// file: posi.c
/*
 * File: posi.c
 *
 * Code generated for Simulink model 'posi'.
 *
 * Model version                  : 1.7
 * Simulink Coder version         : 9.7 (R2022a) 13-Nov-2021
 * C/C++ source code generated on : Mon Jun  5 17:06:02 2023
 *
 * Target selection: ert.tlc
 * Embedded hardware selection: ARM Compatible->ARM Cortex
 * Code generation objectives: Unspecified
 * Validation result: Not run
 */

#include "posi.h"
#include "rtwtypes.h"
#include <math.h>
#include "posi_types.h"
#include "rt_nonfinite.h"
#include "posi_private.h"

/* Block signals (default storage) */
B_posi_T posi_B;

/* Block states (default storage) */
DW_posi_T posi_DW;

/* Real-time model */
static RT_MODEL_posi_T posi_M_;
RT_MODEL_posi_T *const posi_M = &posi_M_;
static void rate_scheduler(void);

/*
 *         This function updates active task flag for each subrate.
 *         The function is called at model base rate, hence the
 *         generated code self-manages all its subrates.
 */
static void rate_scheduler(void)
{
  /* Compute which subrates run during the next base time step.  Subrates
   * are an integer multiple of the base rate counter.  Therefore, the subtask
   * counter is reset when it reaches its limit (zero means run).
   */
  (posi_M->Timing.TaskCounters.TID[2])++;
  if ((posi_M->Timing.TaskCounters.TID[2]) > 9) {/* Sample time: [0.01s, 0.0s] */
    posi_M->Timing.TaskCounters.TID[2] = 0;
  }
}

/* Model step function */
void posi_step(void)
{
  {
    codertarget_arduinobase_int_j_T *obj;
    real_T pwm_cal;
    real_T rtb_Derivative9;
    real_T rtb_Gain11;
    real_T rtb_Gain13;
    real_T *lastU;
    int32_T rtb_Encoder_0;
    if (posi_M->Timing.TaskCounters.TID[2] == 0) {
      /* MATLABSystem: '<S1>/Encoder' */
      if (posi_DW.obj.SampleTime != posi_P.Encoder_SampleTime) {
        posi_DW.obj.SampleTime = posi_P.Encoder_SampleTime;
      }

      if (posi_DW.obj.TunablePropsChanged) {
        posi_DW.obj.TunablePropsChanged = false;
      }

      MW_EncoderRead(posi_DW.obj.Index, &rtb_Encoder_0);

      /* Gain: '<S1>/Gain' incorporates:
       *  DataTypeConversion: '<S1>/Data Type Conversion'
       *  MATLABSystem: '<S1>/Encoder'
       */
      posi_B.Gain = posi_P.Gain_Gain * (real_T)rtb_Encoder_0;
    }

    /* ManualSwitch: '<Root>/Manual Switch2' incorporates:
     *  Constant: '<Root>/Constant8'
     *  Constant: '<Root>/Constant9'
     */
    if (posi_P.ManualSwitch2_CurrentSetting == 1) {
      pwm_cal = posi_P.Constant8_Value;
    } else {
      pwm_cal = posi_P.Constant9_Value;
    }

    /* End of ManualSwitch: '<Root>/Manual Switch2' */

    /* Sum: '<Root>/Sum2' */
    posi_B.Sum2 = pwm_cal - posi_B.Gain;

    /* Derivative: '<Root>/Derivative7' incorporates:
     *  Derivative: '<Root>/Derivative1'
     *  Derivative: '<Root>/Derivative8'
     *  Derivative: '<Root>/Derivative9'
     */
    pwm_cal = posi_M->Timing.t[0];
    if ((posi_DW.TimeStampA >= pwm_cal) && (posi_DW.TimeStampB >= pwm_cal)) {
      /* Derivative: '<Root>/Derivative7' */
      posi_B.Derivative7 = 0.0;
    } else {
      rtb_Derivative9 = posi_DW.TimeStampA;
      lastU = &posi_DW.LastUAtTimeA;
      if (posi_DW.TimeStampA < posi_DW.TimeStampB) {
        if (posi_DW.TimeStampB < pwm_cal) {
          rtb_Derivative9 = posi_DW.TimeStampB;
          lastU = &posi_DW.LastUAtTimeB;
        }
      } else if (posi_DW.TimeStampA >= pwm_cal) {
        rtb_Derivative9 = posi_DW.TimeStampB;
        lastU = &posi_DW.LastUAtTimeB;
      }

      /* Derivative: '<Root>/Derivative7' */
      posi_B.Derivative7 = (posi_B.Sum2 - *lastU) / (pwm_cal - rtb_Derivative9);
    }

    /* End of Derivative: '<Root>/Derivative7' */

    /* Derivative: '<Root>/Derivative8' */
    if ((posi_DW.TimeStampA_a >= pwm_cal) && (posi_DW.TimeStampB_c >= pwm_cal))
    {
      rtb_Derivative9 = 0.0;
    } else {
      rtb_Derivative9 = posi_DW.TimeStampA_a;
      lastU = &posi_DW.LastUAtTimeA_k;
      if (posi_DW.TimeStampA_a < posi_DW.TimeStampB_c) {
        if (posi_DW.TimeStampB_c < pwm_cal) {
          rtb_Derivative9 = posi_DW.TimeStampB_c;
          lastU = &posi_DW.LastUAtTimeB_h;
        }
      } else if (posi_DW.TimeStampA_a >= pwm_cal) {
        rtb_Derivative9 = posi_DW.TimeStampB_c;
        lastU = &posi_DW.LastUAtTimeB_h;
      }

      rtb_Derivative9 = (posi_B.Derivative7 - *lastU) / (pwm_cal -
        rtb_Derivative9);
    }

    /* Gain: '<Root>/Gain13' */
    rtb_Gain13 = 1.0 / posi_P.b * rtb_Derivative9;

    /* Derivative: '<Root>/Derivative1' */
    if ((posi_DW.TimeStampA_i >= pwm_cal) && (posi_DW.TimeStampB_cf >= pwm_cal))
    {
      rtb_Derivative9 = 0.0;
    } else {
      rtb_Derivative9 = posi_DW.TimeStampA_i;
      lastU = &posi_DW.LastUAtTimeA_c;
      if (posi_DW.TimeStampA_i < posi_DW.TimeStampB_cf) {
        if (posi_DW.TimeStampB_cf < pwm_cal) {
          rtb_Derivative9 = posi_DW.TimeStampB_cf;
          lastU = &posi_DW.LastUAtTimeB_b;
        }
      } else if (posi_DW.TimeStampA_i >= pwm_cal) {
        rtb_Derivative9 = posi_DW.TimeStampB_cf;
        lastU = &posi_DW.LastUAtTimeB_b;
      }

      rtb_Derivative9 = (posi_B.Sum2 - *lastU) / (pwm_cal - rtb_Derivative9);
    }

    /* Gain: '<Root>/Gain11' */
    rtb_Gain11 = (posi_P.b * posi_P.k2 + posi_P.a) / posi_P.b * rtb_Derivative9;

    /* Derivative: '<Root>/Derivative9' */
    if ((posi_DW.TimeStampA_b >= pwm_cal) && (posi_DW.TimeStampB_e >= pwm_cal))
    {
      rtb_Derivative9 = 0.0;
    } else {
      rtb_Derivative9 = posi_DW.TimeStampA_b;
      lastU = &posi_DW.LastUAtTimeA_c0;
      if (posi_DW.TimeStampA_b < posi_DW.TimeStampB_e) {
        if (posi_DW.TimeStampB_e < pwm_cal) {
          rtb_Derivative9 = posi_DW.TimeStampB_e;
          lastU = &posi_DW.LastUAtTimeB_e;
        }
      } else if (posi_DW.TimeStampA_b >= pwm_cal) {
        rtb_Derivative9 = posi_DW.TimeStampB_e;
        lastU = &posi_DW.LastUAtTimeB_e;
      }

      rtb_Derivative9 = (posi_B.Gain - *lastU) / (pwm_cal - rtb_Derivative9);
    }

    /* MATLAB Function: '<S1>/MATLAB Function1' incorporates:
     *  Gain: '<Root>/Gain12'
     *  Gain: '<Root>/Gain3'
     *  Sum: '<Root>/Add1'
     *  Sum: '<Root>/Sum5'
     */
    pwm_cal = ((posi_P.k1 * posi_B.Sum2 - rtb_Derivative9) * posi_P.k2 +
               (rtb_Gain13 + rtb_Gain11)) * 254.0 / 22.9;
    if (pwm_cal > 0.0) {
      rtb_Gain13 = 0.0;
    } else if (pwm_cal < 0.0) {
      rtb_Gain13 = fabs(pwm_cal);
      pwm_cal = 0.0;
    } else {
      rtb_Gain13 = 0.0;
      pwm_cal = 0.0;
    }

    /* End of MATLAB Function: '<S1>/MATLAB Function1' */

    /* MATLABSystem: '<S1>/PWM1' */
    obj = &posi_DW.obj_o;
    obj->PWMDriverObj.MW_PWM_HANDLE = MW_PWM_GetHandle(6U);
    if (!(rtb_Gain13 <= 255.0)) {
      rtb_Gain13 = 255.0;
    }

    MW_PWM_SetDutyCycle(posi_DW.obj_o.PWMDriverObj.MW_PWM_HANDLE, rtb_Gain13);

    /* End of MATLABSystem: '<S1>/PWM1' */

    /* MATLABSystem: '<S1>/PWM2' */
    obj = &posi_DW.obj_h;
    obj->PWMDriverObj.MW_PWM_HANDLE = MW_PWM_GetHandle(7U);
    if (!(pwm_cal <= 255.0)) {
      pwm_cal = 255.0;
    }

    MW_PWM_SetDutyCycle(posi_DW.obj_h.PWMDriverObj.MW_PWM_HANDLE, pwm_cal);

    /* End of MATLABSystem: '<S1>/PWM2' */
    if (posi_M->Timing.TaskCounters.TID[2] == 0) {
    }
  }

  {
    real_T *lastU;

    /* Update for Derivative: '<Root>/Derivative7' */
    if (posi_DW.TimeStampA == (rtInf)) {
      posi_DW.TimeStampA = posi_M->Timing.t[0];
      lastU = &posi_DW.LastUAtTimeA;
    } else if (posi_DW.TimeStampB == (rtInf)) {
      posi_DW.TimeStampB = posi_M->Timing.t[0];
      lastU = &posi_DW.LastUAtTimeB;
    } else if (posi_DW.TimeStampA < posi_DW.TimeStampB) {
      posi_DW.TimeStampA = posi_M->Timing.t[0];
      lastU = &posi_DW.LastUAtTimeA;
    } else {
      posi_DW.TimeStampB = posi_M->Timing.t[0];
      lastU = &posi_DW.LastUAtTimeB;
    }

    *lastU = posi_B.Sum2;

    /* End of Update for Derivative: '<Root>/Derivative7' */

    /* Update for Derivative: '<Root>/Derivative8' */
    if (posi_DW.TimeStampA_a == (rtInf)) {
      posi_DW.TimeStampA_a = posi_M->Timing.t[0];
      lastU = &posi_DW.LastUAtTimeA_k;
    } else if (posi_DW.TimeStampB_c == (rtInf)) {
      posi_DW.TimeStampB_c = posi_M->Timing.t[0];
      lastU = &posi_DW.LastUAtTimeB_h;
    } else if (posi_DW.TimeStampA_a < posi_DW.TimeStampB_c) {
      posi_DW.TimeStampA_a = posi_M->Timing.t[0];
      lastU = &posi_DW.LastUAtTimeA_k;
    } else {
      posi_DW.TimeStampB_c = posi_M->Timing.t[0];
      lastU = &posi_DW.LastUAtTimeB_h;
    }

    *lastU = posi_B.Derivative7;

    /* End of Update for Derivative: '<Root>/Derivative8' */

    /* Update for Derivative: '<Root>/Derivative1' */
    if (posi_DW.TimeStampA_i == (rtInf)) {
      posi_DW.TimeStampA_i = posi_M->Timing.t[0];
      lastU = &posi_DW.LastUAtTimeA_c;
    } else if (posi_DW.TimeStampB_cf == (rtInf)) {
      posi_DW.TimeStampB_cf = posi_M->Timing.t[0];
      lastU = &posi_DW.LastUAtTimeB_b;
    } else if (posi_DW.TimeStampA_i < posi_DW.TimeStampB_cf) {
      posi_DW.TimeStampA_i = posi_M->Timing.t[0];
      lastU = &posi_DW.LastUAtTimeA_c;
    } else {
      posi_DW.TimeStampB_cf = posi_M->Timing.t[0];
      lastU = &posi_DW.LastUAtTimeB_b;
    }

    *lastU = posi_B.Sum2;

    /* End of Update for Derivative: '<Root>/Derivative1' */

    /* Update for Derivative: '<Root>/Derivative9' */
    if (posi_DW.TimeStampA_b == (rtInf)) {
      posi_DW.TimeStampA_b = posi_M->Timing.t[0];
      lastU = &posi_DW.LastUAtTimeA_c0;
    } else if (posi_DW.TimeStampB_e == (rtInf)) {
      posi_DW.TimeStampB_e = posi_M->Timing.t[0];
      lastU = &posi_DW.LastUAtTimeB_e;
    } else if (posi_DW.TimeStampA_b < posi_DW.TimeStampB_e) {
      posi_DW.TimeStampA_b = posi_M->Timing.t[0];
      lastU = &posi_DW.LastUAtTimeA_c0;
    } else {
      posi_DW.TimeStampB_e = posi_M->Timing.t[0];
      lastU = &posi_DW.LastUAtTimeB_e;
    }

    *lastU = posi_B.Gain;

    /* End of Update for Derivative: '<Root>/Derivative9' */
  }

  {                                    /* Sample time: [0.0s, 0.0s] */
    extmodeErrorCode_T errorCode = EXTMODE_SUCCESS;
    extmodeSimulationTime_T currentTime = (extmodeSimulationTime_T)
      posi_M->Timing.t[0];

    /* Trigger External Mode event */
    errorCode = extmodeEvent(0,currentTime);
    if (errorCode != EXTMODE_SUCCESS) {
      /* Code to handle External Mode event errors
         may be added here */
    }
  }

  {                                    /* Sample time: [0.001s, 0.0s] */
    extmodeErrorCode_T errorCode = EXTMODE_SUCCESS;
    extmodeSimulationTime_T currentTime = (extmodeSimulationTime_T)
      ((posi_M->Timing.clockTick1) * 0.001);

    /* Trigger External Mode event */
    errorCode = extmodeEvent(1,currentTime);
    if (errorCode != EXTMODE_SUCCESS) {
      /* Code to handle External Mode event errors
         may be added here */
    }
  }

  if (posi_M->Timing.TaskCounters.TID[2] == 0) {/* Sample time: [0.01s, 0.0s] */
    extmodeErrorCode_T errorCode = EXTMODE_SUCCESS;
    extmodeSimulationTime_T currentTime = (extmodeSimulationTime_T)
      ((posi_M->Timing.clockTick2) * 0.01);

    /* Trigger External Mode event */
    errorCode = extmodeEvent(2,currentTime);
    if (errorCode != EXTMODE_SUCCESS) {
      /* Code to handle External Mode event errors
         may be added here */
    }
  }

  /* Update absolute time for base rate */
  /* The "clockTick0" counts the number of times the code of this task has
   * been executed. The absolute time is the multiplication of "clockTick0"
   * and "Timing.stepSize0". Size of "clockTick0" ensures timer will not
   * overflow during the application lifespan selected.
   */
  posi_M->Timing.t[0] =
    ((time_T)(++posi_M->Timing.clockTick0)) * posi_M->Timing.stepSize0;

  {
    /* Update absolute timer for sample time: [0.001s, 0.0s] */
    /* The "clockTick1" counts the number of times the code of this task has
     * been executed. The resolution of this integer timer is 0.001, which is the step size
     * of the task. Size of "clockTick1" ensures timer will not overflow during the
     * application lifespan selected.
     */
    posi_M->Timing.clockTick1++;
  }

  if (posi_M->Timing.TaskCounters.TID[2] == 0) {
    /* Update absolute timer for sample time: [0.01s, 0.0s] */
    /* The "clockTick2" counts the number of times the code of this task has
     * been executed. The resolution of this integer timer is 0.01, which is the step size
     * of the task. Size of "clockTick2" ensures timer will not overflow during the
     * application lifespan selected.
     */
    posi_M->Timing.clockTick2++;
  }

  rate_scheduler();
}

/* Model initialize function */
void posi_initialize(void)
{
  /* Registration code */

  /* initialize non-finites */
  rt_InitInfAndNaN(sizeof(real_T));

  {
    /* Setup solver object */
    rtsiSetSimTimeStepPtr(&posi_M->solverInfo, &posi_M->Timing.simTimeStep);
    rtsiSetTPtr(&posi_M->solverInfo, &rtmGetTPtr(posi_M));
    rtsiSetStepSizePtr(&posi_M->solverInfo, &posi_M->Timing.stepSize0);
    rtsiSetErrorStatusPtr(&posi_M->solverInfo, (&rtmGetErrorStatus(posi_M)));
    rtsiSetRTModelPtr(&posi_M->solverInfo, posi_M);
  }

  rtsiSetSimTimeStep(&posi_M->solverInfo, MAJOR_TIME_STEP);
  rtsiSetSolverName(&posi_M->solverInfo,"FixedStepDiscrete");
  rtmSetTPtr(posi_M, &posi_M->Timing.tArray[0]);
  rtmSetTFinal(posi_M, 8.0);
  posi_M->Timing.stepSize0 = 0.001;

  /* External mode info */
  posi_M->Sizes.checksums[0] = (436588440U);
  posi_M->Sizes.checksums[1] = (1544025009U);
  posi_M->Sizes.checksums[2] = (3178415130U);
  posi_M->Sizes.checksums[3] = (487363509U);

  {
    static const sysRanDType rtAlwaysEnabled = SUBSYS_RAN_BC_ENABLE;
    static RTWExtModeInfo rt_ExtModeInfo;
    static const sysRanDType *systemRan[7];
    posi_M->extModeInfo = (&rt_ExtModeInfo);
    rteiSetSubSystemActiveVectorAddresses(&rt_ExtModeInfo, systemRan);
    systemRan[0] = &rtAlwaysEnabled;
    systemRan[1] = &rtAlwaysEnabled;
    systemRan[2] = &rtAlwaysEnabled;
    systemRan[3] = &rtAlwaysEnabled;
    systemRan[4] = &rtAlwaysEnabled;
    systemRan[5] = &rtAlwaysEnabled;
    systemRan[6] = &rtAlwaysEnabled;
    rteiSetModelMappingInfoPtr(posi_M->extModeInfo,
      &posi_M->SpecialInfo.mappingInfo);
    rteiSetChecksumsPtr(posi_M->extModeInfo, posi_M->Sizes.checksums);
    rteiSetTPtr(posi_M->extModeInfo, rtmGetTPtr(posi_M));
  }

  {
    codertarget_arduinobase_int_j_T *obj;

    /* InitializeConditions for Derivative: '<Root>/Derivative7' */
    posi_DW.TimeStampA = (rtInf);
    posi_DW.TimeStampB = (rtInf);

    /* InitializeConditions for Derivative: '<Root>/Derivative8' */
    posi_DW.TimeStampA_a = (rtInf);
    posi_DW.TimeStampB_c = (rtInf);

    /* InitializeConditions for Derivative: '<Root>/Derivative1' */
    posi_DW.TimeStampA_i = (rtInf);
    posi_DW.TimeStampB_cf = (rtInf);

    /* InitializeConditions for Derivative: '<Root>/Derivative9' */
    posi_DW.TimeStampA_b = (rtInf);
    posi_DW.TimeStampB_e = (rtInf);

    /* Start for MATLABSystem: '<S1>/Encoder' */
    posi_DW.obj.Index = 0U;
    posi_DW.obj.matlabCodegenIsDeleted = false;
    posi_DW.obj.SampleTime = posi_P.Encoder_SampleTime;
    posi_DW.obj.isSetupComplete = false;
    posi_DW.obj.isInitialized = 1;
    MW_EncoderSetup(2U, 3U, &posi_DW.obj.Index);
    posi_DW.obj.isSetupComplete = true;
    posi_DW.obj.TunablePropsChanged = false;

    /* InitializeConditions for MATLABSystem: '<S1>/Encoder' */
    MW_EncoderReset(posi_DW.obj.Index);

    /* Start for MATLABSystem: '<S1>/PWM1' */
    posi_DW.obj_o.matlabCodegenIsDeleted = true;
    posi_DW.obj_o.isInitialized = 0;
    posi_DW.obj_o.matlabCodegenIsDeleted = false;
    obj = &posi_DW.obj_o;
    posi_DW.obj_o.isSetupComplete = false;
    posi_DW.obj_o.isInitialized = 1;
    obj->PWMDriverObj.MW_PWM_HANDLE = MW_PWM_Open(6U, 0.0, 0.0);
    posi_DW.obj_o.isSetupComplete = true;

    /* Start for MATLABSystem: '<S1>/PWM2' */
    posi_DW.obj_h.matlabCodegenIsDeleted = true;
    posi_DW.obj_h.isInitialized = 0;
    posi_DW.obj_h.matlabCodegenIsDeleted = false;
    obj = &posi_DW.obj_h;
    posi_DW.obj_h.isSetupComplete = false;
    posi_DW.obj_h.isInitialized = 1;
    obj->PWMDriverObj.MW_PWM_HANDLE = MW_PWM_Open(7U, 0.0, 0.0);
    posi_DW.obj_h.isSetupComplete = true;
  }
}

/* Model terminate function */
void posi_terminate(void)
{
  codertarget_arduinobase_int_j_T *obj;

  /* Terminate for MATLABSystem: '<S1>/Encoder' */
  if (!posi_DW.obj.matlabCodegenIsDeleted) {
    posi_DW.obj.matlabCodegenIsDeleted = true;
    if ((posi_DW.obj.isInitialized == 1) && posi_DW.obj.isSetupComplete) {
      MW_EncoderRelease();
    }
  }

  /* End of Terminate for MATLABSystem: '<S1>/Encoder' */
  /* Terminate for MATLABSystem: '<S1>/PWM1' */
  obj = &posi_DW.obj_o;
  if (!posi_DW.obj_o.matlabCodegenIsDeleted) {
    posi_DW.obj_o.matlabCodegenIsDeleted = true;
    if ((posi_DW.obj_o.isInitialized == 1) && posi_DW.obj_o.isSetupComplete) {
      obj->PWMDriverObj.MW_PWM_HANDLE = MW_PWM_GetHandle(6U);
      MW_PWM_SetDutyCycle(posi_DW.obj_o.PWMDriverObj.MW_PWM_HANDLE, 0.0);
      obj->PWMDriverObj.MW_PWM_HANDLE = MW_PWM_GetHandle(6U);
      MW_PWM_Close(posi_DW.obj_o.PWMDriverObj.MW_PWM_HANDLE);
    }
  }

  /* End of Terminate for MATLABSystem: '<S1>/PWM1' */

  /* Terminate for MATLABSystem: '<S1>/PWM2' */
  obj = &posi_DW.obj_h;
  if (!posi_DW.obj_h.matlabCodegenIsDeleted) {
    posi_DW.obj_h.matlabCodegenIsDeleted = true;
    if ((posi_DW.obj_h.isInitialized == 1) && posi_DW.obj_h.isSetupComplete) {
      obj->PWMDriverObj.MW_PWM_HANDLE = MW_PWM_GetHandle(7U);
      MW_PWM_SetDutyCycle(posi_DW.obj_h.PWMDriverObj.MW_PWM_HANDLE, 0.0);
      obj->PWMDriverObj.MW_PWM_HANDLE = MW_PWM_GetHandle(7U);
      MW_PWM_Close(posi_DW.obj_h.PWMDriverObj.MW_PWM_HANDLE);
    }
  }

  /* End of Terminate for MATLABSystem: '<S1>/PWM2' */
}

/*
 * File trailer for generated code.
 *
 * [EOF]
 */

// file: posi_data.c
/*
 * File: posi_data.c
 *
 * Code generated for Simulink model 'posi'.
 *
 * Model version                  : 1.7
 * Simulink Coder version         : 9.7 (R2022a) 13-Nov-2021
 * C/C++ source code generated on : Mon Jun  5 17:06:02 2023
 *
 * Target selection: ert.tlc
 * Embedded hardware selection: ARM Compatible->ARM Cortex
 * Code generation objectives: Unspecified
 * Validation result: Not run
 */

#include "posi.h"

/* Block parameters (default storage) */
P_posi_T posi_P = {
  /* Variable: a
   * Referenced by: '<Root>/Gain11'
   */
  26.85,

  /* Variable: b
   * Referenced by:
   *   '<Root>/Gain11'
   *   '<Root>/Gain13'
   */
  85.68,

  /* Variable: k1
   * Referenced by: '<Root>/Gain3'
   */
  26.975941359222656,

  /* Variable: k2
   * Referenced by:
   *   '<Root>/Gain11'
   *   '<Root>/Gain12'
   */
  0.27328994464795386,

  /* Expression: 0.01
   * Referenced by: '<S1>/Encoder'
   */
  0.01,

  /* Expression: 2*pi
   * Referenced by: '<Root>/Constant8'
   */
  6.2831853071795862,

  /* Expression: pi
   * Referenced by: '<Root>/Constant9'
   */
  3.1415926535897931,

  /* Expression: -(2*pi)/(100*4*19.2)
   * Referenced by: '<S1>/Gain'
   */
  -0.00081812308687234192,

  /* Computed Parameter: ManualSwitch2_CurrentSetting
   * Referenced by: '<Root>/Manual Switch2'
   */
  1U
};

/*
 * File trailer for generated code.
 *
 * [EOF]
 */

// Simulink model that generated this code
simulink model "posi"  (R2022a)
settings: Solver=ode1  StartTime=0.0  StopTime=8  FixedStep=0.001  RelTol=1e-3
undefined symbols (not defined in the file or in its folder): a, b, k1, k2
libraries: arduinolib x4, arduinosensorlib x1

== system posi ==
  note: $\theta$
  Add1 : Sum  Inputs=+++
  Constant8 : Constant  Value=2*pi
  Constant9 : Constant  Value=pi
  Derivative{1,7..9} (4 alike) : Derivative
  Gain11 : Gain  Gain=(a+b*k2)/b
  Gain12 : Gain  Gain=k2
  Gain13 : Gain  Gain=1/b
  Gain3 : Gain  Gain=k1
  Manual Switch2 : ManualSwitch
  Right motor1 : Subsystem
  Scope : Scope
  Scope7 : Scope
  Sum2 : Sum  Inputs=|+-
  Sum5 : Sum  Inputs=|+-
  wires:
  Derivative7/1 -> Derivative8/1
  Constant8/1 -> Manual Switch2/1
  Derivative1/1 -> Gain11/1
  Right motor1/1(outGearBox) -> Sum2/2, Derivative9/1, Scope7/1
  Gain12/1 -> Add1/3
  Gain3/1 -> Sum5/1
  Derivative8/1 -> Gain13/1
  Derivative9/1 -> Sum5/2
  Sum5/1 -> Gain12/1
  Gain13/1 -> Add1/1
  Constant9/1 -> Manual Switch2/2
  Gain11/1 -> Add1/2
  Manual Switch2/1 -> Sum2/1
  Add1/1 -> Right motor1/1(v_a)
  Sum2/1 -> Derivative7/1, Derivative1/1, Scope/1, Gain3/1

== system posi/Right motor1 ==
  v_a : Inport
  Convert pulse to rad1 : MATLAB Function  Commented=on  TreatAsAtomicUnit=on
  Data Type Conversion : DataTypeConversion  OutDataTypeStr=double  SaturateOnIntegerOverflow=off  RndMeth=Floor
  Digital Output : arduinolib/Digital Output  Commented=on  pinNumber=7  Direction=output  blockPlatform=arduino
  Encoder : arduinosensorlib/Encoder  InputA=2  InputB=3  Mode=No reset  SampleTime=0.01
  Encoder1 : S-Function  Commented=on  InitFcn=try, set_param(gcb,'FunctionName','readEncDUEpin8_9'), end  FunctionName=readEncDUEpin8_9  SFunctionModules=readEncDUEpin8_9_wrapper  SFunctionDeploymentMode=off  EnableBusSupport=off  mask(S-Function Builder){}
      mask help: Simulink:masks:SFunctionBuilder_MD
      mask init:
      | val = [[.9  0.75 0.75 1 1 .9 .9 1]',[1 1 0.75 0.75 .9 .9 1 .9]'];try , sys = get_param(gcb,'SfunBuilderFcnName');if isempty(sys), sys = get_param(gcb,'FunctionName'); end,catch, sys = get_param(gcb,'FunctionName'); end
  Gain : Gain  Gain=-(2*pi)/(100*4*19.2)
  MATLAB Function1 : MATLAB Function  TreatAsAtomicUnit=on
  MATLAB Function2 : MATLAB Function  Commented=on  TreatAsAtomicUnit=on
  PWM : arduinolib/PWM  Commented=on  pinNumber=5  frequencyType=Default  desiredFrequency=490.2  achievableFrequency=490.2
  PWM1 : arduinolib/PWM  pinNumber=6  frequencyType=Default  desiredFrequency=490.2  achievableFrequency=490.2
  PWM2 : arduinolib/PWM  pinNumber=7  frequencyType=Default  desiredFrequency=490.2  achievableFrequency=490.2
  Scope : Scope  Commented=on
  Scope1 : Scope
  gearRatio : Constant  Commented=on  Value=336
  totalPPR : Constant  Commented=on  Value=16*2
  outGearBox : Outport
  wires:
  Gain/1 -> Scope1/1, outGearBox/1
  Encoder/1 -> Data Type Conversion/1
  v_a/1 -> MATLAB Function1/1(v_a)
  MATLAB Function1/2(Rpwm) -> PWM2/1
  MATLAB Function1/1(Lpwm) -> PWM1/1
  Encoder1/1 -> Convert pulse to rad1/1(u)
  Convert pulse to rad1/1(outGearBox) -> Scope/1
  gearRatio/1 -> Convert pulse to rad1/3(gearRatio)
  MATLAB Function2/1(pwm) -> PWM/1
  MATLAB Function2/2(dir) -> Digital Output/1
  totalPPR/1 -> Convert pulse to rad1/2(ppr)
  Data Type Conversion/1 -> Gain/1

== matlab function posi/Right motor1/Convert pulse to rad1 ==
  settings: updateMethod=DISCRETE
function outGearBox = fcn(u,ppr,gearRatio)

persistent counter_num over_flag
if(isempty(counter_num)), counter_num = 0;end
if(isempty(over_flag)), over_flag = 0;end
pulse2radian = 2*pi/ppr; % 1 pulse = ?? radian

if(double(u) - counter_num > 40000), over_flag = over_flag-1;
elseif(double(u) - counter_num < -40000), over_flag = over_flag+1;
end

inGearBox = (double(u)+over_flag*(2^32 -1))*pulse2radian; 
outGearBox = inGearBox/gearRatio;
counter_num = double(u) ;

== matlab function posi/Right motor1/MATLAB Function1 ==
function [Lpwm,Rpwm] = fcn(v_a)

vmax = 22.9;
pwm_cal = v_a*254/vmax;

if pwm_cal > 0
    Lpwm = 0;
    Rpwm = pwm_cal;
elseif pwm_cal < 0
    Lpwm = abs(pwm_cal);
    Rpwm = 0;
else
    Lpwm = 0;
    Rpwm = 0;
end

== matlab function posi/Right motor1/MATLAB Function2 ==
function [pwm,dir] = fcn(v_a)

vmax = 22.9;
%vmax = 10;
pwm_cal = v_a*254/vmax;
if pwm_cal > 0
    pwm = pwm_cal;
    dir = 0;
elseif pwm_cal < 0
    pwm = abs(pwm_cal);
    dir = 1;
else
    pwm = 0;
    dir = 0;
end
